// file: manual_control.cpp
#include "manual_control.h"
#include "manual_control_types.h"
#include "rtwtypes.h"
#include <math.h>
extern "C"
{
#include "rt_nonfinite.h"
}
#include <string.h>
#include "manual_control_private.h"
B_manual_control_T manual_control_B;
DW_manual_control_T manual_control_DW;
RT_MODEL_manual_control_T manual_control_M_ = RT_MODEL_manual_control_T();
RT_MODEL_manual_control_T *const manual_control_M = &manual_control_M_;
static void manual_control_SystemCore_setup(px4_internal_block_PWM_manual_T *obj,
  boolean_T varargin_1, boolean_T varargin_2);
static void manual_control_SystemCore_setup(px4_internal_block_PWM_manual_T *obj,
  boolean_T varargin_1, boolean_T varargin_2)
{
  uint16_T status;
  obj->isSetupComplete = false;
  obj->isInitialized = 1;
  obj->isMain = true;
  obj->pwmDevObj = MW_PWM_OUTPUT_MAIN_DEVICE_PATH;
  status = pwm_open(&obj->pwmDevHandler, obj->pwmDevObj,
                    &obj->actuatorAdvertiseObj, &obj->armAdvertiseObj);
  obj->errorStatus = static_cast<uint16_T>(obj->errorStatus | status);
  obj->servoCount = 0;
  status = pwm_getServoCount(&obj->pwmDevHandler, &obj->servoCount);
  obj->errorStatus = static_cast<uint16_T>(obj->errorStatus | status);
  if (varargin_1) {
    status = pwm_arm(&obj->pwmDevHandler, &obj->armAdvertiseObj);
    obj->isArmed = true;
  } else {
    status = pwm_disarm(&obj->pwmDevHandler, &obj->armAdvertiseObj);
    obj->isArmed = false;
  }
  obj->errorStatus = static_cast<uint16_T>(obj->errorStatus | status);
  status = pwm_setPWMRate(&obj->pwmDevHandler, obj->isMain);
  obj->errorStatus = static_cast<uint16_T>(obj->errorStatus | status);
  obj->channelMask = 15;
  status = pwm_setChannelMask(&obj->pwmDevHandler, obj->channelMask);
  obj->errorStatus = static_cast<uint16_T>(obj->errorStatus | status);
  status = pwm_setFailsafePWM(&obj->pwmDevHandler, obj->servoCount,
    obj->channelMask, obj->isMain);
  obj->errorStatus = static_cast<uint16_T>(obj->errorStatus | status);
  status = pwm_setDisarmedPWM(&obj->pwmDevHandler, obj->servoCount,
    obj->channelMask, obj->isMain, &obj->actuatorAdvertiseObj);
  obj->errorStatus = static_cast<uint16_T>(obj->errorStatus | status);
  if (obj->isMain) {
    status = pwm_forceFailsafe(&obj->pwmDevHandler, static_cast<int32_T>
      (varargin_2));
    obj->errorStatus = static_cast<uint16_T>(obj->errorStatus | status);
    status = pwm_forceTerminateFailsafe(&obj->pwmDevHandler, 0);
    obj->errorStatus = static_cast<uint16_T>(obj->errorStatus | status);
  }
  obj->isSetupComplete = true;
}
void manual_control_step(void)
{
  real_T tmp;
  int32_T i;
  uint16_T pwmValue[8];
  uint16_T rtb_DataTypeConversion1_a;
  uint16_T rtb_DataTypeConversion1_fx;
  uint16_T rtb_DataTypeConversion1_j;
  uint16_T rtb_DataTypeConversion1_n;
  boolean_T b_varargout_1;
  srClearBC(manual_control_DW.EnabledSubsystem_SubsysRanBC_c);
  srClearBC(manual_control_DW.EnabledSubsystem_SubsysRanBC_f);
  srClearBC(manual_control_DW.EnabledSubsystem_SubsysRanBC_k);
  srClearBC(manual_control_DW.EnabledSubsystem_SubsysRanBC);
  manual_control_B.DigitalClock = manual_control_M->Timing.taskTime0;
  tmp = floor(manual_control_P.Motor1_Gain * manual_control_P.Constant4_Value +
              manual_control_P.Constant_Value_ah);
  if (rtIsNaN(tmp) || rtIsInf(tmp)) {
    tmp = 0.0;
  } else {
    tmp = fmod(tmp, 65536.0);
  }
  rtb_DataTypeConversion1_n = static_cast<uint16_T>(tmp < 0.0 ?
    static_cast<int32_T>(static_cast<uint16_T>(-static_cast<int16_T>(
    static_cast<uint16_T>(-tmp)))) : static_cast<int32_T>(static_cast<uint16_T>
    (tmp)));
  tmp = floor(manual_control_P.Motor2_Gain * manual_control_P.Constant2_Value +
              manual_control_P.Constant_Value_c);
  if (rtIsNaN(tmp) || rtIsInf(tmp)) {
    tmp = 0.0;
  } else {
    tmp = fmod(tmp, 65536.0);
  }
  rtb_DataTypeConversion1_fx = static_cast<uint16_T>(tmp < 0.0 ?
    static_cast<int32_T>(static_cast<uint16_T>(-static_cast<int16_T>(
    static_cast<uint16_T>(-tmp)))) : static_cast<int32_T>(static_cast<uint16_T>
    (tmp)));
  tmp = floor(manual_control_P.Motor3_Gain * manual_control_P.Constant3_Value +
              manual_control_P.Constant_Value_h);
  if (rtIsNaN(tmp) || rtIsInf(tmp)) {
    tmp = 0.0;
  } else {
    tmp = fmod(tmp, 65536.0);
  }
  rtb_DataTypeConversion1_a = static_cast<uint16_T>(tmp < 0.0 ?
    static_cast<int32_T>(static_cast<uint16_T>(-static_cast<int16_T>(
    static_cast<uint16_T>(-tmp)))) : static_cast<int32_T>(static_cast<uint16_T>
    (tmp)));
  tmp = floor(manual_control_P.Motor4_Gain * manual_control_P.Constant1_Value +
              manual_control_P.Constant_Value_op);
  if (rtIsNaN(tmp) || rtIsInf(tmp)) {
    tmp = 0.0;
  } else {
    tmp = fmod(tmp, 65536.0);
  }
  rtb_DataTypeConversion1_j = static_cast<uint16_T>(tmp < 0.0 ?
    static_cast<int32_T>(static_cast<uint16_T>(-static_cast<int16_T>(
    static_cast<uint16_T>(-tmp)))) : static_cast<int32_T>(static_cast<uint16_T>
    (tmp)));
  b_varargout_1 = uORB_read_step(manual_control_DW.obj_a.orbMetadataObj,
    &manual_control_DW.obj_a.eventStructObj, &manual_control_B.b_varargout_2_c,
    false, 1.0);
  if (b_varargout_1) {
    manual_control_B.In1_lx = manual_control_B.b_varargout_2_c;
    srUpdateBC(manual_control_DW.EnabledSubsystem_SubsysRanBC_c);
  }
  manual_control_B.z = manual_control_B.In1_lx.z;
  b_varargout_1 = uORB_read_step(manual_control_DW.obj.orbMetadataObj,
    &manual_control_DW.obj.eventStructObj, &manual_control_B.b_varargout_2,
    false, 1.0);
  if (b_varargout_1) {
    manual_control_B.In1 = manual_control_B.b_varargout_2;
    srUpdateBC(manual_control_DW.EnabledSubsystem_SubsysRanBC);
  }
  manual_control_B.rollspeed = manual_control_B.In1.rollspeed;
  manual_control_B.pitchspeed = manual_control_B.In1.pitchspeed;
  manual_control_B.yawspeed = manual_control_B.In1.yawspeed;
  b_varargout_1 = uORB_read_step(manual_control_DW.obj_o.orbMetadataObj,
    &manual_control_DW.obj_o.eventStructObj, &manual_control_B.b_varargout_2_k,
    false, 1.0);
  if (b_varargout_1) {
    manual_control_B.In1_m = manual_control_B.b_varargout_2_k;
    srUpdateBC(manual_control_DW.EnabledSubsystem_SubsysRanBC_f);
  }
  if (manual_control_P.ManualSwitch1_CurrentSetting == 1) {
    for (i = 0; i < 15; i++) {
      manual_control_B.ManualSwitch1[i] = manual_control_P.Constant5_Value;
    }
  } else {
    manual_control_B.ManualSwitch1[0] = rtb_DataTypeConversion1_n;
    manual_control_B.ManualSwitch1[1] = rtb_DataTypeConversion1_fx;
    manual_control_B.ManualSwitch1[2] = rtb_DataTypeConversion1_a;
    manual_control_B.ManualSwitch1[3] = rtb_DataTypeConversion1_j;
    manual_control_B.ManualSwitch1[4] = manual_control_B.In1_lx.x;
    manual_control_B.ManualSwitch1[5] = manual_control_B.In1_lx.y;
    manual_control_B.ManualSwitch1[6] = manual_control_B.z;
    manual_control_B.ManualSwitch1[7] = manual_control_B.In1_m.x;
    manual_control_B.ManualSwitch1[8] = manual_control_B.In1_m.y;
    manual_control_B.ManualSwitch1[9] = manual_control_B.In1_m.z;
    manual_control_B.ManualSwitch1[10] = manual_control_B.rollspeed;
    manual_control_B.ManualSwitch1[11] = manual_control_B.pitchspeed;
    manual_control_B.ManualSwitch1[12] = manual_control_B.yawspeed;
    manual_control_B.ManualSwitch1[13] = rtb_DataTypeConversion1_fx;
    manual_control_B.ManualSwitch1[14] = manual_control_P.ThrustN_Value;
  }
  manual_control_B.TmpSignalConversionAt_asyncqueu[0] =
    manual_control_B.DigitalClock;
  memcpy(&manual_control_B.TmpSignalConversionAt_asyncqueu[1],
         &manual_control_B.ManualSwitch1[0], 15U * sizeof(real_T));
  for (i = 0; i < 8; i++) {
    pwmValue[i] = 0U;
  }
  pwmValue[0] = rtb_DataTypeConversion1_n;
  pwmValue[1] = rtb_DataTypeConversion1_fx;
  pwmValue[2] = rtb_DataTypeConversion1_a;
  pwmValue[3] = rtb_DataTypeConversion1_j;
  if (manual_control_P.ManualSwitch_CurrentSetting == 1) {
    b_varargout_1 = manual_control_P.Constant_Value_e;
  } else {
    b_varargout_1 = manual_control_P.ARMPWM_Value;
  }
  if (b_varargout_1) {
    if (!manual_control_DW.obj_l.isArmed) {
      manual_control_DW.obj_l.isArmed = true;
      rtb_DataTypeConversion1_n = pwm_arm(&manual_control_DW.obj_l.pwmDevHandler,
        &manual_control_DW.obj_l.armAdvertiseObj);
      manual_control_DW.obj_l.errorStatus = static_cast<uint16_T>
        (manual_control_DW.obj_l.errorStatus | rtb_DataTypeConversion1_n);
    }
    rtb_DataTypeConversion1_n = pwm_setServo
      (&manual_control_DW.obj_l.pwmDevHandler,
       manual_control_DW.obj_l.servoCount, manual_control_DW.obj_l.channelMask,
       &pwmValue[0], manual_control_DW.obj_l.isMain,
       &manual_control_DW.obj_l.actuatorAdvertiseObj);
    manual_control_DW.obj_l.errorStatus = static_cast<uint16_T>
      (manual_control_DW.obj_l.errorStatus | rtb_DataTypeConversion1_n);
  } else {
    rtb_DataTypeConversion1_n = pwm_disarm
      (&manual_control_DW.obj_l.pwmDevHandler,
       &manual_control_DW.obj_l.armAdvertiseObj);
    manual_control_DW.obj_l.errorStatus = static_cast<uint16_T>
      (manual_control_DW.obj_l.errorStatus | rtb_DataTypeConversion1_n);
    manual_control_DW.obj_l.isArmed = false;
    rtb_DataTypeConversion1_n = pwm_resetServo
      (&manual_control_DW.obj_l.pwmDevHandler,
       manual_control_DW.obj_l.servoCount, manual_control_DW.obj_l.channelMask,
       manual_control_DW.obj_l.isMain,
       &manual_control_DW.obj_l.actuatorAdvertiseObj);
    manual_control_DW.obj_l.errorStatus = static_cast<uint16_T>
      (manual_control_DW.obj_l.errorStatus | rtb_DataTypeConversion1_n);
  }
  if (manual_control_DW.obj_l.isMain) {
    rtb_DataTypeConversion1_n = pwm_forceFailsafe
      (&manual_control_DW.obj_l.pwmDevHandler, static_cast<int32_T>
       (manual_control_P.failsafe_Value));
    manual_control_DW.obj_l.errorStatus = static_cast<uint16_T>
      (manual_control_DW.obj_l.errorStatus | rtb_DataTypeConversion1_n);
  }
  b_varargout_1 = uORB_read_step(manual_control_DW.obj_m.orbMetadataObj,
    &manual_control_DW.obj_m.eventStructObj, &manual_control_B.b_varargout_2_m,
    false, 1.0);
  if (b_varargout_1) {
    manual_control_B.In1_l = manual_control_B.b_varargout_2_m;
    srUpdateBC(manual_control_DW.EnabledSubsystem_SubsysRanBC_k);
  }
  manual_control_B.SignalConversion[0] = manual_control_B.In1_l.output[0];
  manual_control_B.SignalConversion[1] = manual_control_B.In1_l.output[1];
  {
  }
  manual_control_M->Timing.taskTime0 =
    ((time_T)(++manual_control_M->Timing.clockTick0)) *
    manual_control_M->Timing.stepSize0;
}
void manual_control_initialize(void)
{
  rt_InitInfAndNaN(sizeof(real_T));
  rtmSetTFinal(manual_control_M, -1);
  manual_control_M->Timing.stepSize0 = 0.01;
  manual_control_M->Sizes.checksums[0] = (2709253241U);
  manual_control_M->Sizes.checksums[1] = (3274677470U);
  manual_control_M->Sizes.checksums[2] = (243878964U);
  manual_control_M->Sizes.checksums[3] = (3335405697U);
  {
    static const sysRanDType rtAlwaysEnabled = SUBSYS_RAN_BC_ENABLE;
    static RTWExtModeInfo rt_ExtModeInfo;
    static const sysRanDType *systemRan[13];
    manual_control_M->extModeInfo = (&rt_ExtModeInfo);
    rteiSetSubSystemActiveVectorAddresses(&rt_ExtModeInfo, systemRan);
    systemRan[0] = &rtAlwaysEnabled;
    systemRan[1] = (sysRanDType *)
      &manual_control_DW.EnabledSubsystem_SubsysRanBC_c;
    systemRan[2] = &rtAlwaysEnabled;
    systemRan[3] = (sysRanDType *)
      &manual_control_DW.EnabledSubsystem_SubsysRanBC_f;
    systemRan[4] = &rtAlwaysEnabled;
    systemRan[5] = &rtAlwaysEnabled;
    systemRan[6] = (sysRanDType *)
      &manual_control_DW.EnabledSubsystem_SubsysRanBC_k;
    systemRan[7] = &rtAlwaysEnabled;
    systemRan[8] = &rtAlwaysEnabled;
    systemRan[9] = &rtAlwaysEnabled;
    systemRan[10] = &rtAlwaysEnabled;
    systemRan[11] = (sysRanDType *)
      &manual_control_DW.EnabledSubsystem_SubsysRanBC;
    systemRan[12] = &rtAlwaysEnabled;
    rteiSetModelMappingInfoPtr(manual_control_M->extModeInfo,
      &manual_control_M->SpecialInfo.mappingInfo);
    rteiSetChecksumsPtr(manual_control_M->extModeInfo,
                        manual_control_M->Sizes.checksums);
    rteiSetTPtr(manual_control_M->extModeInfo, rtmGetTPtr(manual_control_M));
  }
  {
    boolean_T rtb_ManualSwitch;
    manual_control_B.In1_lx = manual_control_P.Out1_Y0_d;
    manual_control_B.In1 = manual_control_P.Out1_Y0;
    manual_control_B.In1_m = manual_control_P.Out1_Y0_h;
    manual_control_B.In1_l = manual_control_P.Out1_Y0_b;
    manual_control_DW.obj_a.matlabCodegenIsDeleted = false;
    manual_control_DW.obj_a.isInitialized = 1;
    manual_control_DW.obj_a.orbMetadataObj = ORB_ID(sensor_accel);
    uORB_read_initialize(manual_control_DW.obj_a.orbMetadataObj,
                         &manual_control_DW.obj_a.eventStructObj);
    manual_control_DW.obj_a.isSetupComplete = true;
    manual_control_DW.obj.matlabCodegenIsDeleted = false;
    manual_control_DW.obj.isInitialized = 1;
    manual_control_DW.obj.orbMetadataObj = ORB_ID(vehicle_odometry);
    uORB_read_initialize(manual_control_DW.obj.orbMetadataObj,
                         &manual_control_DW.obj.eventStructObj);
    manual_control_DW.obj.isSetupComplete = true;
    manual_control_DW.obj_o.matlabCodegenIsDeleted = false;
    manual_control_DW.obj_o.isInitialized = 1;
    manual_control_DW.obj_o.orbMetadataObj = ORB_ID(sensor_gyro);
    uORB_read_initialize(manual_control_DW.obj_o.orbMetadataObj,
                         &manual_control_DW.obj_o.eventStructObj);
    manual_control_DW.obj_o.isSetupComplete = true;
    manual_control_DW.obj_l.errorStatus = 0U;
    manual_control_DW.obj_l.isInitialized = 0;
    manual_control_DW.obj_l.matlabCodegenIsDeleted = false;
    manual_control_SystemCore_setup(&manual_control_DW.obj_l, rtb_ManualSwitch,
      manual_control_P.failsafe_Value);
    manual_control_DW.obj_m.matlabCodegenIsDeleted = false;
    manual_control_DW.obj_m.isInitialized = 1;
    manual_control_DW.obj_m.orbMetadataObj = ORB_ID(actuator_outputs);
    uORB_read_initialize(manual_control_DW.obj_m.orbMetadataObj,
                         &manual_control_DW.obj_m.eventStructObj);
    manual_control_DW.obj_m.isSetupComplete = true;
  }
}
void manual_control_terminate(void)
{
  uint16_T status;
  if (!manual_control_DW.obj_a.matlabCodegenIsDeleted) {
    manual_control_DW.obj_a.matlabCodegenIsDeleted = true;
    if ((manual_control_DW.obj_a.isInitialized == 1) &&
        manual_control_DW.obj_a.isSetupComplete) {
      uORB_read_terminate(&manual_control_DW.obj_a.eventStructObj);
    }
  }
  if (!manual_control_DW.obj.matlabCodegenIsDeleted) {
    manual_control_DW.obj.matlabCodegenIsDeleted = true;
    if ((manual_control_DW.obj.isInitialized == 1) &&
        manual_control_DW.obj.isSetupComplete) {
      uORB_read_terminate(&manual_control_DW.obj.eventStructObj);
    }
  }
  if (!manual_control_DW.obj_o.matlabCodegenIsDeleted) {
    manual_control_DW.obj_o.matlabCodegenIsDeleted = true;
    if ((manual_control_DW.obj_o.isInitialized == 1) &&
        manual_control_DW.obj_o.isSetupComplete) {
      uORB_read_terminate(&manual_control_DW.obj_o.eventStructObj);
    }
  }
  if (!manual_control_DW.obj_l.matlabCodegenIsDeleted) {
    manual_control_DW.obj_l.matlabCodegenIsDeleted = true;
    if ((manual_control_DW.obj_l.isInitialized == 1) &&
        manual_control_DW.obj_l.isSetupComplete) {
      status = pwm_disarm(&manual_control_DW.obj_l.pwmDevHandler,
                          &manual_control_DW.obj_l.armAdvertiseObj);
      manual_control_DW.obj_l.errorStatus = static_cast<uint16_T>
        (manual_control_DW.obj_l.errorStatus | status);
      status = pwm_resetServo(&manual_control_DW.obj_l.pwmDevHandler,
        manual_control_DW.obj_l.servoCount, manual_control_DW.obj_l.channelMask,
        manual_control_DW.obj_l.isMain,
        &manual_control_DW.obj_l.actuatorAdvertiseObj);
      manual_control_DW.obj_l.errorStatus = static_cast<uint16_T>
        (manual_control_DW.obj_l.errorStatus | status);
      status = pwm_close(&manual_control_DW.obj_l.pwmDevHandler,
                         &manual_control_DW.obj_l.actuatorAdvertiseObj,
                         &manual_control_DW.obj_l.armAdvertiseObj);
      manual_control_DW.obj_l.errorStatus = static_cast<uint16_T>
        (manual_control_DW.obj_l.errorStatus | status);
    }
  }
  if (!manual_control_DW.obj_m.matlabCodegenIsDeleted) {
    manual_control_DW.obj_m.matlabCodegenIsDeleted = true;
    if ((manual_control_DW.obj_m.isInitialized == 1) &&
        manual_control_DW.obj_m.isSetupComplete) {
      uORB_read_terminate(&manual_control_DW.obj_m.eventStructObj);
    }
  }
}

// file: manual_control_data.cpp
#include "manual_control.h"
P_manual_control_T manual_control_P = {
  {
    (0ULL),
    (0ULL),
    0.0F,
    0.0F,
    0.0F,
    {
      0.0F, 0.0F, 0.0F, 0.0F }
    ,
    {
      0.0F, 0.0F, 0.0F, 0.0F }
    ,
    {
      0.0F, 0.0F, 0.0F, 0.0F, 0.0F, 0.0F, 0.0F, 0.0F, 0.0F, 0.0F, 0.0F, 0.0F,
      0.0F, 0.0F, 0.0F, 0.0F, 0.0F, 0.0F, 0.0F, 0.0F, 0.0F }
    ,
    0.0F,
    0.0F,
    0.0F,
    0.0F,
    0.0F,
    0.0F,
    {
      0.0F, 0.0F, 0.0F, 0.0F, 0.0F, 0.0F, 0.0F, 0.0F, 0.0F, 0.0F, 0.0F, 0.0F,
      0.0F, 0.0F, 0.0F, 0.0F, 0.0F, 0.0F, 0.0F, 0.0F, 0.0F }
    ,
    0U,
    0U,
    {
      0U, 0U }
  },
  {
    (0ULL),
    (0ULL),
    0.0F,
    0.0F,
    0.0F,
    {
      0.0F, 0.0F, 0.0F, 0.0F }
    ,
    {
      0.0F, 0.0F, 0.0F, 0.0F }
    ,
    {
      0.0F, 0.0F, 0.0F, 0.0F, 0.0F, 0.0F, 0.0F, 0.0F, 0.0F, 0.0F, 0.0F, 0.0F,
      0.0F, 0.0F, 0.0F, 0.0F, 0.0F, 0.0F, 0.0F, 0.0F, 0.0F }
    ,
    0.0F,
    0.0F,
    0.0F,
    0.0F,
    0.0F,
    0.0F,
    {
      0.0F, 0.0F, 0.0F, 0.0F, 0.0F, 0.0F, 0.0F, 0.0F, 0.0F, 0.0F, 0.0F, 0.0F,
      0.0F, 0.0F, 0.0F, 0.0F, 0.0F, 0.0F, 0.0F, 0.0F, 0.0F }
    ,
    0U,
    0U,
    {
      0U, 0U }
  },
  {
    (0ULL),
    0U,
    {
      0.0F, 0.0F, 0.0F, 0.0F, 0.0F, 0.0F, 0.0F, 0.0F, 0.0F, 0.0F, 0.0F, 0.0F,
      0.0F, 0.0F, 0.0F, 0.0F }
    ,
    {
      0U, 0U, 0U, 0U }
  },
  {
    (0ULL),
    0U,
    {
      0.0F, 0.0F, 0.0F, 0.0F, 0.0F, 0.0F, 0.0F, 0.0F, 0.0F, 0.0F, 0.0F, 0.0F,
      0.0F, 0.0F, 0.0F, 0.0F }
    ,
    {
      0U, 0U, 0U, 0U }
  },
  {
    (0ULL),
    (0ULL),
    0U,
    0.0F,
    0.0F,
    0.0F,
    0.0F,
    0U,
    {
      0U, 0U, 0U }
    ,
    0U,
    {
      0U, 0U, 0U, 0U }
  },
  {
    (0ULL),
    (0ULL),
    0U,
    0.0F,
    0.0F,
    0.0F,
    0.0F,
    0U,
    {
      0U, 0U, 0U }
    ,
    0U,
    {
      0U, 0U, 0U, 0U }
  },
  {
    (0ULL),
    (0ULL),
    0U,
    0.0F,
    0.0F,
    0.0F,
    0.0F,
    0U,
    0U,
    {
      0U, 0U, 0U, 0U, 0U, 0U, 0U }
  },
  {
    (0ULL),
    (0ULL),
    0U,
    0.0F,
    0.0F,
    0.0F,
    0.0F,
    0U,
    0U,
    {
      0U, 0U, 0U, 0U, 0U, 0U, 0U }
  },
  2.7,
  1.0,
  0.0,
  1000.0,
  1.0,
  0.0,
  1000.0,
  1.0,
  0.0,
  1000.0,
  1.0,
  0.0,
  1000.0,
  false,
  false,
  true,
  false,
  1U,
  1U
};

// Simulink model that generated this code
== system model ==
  DigitalClock : DigitalClock
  Sum#1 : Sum  Inputs=+-  <- 1: Integrator#1, 2: Constant#1
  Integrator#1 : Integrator
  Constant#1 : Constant  Value=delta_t
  CustomTuningWebBlock#1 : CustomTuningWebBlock
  ManualSwitch1 : ManualSwitch  <- 1: Constant5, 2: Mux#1
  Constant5 : Constant  Value=0
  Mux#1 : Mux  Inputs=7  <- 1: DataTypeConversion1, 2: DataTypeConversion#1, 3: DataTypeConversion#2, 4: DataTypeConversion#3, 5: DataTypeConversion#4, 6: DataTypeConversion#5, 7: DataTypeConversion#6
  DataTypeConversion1 : DataTypeConversion  <- 1: DataTypeConversion#7
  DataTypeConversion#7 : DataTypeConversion  <- 1: Sum#2
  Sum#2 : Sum  Inputs=++  <- 1: Motor1, 2: Constant
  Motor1 : Gain  Gain=0  <- 1: Constant4
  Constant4 : Constant
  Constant : Constant  Value=1000
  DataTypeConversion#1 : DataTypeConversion  <- 1: DataTypeConversion#8
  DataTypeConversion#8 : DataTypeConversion  <- 1: Sum#3
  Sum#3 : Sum  Inputs=++  <- 1: Motor2, 2: Constant#2
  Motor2 : Gain  Gain=0  <- 1: Constant2
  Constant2 : Constant
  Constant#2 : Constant  Value=1000
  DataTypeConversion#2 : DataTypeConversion  <- 1: DataTypeConversion#9
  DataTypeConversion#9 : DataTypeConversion  <- 1: Sum#4
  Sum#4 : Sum  Inputs=++  <- 1: Motor3, 2: Constant#3
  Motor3 : Gain  Gain=0  <- 1: Constant3
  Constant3 : Constant
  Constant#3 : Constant  Value=1000
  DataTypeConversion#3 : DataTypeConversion  <- 1: DataTypeConversion#10
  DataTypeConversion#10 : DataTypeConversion  <- 1: Sum#5
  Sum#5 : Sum  Inputs=++  <- 1: Motor4, 2: Constant#4
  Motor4 : Gain  Gain=0  <- 1: Constant1
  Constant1 : Constant
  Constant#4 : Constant  Value=1000
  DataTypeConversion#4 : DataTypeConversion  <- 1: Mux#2
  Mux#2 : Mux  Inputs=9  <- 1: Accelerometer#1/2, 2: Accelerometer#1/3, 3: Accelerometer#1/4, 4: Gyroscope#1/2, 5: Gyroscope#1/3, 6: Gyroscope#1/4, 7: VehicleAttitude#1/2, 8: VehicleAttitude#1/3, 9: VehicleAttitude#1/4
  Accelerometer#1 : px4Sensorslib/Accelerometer
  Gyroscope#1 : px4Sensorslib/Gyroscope
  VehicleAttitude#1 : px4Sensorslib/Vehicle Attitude
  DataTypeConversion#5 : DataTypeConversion  <- 1: DataTypeConversion#8
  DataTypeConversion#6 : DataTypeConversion  <- 1: ThrustN
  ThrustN : Constant  Value=2.7
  PX4PWMOutput#1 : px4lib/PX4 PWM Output  <- 1: ManualSwitch, 2: failsafe, 3: DataTypeConversion#7, 4: DataTypeConversion#8, 5: DataTypeConversion#9, 6: DataTypeConversion#10
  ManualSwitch : ManualSwitch  <- 1: Constant#5, 2: ARMPWM
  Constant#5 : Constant  Value=0
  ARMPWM : Constant
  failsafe : Constant  Value=0
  SignalConversion : SignalConversion  <- 1: Selector#1
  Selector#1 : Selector  Indices=[1 2]  <- 1: BusSelector#1
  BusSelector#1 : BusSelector  <- 1: PX4uORBRead#1/2
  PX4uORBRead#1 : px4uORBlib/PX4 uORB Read
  CustomTuningWebBlock#2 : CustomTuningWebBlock
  CustomTuningWebBlock#3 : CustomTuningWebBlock
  CustomTuningWebBlock#4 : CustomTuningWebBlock
